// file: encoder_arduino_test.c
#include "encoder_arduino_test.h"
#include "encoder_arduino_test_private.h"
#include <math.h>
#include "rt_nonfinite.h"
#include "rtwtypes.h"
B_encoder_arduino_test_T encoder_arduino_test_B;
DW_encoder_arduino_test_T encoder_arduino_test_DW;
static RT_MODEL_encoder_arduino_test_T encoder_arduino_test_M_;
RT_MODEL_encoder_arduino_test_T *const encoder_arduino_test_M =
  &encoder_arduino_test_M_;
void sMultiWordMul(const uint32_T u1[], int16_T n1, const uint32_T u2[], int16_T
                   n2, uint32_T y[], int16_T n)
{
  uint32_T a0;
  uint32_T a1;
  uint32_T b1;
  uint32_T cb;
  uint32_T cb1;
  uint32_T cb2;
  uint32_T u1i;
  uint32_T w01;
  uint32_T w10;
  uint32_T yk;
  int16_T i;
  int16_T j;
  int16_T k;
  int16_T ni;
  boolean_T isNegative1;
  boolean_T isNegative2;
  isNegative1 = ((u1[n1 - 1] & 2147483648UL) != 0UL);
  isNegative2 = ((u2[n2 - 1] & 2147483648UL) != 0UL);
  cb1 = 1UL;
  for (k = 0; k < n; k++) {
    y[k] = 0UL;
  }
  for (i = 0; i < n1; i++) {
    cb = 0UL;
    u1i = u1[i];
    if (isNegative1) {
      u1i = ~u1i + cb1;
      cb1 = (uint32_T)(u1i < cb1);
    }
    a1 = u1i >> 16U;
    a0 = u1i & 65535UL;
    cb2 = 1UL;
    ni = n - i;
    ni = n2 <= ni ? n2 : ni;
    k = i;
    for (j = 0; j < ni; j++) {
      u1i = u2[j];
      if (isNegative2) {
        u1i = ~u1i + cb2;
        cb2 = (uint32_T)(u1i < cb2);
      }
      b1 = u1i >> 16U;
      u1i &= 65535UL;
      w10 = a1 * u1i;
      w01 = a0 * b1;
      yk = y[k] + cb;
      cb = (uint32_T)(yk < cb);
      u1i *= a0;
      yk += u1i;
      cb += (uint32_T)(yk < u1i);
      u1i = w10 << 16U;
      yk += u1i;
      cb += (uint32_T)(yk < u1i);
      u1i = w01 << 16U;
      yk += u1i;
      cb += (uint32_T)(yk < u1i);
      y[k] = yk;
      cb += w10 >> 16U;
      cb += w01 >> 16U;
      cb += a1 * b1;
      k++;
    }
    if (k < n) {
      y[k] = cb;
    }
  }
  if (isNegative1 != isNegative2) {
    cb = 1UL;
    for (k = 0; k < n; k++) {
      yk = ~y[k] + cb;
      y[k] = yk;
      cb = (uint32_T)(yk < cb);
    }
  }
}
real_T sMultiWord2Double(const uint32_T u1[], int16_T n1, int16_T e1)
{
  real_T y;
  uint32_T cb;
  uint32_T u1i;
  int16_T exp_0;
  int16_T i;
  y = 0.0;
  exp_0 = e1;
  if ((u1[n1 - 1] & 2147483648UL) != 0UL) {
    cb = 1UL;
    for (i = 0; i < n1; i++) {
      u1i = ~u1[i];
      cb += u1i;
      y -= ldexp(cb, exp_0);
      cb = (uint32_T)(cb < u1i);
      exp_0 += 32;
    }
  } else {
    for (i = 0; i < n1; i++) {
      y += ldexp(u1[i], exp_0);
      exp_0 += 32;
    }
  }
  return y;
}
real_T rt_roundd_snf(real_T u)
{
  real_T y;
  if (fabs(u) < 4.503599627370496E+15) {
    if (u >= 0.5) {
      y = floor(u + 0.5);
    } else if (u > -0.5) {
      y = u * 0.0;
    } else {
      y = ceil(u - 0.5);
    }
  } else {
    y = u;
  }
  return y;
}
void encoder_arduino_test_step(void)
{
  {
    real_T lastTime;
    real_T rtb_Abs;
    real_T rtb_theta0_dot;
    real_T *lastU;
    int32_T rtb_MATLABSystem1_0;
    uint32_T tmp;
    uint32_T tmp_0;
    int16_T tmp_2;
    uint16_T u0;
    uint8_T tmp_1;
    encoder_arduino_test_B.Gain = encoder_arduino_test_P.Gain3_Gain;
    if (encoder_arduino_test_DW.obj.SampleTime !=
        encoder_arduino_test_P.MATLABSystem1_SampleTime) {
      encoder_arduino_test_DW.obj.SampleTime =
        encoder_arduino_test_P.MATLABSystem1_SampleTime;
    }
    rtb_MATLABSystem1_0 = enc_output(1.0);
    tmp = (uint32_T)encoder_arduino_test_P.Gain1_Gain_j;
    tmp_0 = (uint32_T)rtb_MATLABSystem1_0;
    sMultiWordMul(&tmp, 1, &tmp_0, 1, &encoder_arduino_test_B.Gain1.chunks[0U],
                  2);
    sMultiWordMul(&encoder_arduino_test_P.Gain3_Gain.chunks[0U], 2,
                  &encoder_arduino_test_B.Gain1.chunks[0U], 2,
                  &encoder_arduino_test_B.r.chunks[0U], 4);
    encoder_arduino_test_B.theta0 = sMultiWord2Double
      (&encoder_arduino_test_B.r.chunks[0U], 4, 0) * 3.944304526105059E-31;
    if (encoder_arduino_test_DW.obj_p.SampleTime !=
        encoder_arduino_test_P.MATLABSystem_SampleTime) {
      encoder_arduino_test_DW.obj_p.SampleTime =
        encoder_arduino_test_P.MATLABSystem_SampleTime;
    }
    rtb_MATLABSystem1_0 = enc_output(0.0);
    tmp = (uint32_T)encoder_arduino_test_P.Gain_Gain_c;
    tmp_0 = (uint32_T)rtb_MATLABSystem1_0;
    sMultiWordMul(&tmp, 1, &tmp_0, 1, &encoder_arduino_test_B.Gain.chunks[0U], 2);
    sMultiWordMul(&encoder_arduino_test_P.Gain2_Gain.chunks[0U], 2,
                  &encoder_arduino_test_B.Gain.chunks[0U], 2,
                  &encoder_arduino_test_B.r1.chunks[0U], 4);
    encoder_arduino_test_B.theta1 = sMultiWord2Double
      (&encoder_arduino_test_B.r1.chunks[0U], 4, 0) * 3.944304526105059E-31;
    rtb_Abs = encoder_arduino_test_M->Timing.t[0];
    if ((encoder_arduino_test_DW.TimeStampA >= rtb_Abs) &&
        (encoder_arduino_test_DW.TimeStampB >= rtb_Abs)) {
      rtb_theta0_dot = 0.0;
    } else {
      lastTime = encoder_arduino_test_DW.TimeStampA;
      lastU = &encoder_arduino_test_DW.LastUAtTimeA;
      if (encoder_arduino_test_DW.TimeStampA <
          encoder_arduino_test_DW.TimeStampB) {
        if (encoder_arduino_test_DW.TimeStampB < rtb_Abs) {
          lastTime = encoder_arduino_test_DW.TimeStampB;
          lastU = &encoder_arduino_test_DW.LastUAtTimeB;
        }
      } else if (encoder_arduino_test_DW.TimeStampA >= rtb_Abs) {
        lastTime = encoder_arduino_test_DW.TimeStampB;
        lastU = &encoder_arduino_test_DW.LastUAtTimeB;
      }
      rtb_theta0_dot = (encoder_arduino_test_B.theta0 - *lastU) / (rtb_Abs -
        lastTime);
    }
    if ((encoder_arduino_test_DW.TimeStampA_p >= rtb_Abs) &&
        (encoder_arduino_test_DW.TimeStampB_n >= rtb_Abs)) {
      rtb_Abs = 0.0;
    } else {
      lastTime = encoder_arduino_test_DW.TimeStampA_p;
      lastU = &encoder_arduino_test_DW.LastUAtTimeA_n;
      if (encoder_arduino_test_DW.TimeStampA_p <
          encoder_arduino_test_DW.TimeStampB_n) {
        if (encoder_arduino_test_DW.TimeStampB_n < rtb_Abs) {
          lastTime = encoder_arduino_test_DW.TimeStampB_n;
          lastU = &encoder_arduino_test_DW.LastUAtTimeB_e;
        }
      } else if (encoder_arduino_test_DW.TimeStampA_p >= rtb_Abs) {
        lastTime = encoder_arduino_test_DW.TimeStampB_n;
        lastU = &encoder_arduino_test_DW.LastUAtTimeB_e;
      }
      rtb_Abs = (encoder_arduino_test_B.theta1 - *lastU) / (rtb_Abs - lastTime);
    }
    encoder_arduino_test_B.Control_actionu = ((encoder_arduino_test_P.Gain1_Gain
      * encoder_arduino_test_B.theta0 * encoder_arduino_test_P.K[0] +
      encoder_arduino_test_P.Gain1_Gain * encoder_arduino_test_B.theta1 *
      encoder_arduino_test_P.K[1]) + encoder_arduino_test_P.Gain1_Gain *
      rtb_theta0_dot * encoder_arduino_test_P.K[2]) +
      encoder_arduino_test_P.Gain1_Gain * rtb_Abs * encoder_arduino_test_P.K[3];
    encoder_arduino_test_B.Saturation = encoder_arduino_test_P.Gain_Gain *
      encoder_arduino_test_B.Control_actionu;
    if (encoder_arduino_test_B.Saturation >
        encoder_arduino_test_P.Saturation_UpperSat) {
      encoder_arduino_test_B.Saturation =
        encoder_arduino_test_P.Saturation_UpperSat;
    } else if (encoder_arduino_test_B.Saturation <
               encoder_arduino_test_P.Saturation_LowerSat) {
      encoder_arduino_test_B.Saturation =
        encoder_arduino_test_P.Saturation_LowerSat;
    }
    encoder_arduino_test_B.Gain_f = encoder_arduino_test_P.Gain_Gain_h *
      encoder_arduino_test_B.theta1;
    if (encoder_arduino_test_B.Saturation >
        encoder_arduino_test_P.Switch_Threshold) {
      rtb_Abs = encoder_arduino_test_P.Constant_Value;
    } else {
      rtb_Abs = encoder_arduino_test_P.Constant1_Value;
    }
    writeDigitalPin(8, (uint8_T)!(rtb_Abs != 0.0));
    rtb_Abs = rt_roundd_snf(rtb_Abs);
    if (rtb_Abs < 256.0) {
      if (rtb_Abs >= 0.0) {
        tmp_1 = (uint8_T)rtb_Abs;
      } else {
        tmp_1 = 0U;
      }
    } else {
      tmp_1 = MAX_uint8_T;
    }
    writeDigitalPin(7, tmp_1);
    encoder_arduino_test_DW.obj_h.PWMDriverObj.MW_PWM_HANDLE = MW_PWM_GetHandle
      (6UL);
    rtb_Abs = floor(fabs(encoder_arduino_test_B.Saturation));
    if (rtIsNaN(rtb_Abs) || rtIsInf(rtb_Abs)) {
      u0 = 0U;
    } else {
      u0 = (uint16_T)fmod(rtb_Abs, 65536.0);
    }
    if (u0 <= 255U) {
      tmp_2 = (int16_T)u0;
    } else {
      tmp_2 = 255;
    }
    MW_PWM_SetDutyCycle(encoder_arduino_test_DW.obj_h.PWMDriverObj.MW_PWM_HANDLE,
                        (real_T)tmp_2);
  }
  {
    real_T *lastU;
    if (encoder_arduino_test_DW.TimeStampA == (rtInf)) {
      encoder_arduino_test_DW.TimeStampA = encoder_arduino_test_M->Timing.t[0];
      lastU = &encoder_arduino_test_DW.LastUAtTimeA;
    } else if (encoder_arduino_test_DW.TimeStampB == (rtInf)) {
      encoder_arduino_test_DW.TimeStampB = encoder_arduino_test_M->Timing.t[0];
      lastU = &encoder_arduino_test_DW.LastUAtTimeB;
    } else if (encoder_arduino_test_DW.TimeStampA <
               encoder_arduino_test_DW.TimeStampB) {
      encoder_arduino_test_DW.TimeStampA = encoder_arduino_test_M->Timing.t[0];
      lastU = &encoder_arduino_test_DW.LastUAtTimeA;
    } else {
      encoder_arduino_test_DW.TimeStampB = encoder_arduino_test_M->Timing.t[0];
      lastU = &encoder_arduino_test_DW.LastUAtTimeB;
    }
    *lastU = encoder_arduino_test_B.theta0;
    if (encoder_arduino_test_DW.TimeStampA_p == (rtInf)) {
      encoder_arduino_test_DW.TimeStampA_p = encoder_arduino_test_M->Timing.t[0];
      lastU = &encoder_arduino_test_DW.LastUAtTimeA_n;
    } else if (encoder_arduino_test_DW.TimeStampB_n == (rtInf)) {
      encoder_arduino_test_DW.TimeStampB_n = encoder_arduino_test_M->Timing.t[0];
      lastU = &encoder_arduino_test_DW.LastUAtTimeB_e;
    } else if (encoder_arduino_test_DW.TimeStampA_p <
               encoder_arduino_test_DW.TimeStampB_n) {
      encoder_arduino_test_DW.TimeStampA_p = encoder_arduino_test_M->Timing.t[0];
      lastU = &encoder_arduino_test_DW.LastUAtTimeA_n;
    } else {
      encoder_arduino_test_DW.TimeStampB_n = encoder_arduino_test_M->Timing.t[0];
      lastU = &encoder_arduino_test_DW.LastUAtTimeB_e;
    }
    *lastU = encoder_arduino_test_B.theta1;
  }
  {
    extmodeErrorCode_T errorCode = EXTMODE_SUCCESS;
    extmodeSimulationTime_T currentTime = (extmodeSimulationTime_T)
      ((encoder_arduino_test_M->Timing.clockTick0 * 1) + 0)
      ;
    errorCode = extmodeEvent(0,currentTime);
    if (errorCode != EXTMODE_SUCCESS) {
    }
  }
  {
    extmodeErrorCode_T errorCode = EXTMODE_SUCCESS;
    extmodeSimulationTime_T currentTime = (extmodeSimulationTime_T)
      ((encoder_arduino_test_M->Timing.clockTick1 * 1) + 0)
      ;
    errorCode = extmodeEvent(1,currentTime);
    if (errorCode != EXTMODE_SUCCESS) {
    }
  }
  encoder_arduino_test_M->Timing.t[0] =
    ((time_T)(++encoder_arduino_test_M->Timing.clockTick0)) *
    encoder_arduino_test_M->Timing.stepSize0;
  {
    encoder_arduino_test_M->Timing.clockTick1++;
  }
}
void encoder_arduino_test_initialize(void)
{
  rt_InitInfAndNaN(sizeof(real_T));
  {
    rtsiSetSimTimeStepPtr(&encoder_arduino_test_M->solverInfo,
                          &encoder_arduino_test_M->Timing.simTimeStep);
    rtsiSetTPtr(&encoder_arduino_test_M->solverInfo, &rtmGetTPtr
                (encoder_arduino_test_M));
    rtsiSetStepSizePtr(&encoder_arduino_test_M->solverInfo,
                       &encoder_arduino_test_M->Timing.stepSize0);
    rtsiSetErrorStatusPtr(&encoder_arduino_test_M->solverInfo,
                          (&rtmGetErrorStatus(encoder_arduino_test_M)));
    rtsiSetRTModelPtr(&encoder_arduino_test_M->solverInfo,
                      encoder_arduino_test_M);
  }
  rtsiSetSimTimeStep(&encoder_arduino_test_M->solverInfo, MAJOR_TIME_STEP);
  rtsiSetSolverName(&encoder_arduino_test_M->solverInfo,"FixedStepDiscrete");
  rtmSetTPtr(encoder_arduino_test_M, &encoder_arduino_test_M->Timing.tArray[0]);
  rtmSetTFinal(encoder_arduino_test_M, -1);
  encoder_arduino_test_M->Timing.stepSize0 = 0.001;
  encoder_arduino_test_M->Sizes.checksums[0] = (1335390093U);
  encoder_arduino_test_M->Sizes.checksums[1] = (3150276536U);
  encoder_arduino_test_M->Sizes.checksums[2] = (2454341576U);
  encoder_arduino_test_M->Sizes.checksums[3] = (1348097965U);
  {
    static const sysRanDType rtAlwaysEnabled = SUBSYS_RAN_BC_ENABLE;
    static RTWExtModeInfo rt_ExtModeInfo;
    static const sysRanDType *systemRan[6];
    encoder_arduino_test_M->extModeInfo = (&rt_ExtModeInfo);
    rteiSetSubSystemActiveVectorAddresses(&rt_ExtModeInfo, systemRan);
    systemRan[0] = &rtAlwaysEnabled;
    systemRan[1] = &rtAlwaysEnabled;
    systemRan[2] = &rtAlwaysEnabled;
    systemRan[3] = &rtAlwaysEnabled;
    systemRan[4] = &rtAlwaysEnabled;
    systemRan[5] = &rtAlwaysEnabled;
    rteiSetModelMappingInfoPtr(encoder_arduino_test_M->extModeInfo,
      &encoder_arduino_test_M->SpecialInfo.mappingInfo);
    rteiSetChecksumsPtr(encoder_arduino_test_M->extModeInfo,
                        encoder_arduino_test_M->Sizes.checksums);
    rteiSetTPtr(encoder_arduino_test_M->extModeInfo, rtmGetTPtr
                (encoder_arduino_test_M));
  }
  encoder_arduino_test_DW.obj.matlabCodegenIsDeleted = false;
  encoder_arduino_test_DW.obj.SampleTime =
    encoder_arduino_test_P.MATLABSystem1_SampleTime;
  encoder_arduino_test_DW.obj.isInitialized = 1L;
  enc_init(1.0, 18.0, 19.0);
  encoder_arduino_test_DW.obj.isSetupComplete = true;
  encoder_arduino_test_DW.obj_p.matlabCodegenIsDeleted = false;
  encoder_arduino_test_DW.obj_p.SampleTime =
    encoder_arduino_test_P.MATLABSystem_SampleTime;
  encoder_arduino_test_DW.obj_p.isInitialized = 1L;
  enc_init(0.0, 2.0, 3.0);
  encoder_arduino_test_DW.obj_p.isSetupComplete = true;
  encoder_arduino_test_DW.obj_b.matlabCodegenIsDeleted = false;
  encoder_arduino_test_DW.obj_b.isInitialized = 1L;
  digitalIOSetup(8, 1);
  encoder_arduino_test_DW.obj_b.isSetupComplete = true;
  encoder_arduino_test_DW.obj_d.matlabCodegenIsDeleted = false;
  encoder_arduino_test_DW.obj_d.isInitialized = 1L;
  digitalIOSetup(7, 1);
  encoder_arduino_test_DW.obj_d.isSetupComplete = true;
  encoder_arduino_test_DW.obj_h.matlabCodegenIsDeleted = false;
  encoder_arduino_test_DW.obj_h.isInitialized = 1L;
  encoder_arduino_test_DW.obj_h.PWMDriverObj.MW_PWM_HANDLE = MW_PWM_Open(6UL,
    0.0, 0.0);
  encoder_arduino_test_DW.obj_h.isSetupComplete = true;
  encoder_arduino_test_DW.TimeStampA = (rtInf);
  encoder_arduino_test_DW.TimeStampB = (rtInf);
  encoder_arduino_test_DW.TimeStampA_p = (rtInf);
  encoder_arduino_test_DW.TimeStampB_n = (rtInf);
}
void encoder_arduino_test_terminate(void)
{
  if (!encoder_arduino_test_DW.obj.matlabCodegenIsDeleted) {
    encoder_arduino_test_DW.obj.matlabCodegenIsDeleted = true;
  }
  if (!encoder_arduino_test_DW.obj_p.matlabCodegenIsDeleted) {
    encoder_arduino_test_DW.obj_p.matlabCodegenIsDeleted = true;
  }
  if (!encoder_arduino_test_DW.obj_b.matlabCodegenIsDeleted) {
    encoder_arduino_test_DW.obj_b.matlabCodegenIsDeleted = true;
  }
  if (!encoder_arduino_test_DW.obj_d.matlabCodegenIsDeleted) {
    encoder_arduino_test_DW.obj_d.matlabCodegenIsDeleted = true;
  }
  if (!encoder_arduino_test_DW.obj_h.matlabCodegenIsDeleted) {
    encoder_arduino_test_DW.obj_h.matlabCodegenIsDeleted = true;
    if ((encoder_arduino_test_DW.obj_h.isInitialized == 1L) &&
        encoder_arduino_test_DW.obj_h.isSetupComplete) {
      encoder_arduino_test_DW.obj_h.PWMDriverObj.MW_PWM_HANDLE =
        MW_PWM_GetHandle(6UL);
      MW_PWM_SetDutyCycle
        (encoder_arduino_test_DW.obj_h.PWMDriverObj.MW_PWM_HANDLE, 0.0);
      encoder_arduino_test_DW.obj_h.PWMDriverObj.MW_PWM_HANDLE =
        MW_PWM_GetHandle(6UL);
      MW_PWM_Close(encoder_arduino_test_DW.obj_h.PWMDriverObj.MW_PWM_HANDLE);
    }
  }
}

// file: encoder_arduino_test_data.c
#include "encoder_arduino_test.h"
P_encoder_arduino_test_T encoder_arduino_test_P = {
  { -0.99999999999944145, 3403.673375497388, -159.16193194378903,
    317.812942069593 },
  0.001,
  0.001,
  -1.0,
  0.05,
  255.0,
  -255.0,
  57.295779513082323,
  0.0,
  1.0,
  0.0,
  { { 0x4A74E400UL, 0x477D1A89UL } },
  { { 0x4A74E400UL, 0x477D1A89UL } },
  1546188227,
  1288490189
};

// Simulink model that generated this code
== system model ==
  Gain : Gain  Gain=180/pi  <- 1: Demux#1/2
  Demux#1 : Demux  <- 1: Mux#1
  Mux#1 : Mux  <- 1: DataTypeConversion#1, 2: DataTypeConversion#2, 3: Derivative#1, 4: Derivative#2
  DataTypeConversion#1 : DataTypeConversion  <- 1: Gain3
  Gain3 : Gain  Gain=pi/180  <- 1: Gain1
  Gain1 : Gain  Gain=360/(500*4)  <- 1: MATLABSystem1
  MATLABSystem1 : MATLABSystem
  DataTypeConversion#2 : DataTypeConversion  <- 1: Gain2
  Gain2 : Gain  Gain=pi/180  <- 1: Gain#1
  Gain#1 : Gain  Gain=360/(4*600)  <- 1: MATLABSystem
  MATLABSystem : MATLABSystem
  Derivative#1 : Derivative  <- 1: DataTypeConversion#1
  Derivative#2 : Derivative  <- 1: DataTypeConversion#2
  DigitalOutput#1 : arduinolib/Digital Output  pinNumber=8  <- 1: Logic#1
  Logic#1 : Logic  Operator=NOT  <- 1: Switch
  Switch : Switch  Criteria=u2 > Threshold  <- 1: Constant, 2: Saturation, 3: Constant1
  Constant : Constant
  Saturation : Saturate  UpperLimit=255  LowerLimit=-255  <- 1: Gain#2
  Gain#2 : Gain  Gain=0.05  <- 1: Gain#3
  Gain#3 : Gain  Gain=K  Multiplication=Matrix(K*u)  <- 1: Gain#4
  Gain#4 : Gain  Gain=-1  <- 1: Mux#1
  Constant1 : Constant  Value=0
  DigitalOutput#2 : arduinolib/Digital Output  pinNumber=7  <- 1: Switch
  PWM : arduinolib/PWM  pinNumber=6  <- 1: DataTypeConversion#3
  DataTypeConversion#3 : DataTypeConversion  <- 1: Abs
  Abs : Abs  <- 1: Saturation
